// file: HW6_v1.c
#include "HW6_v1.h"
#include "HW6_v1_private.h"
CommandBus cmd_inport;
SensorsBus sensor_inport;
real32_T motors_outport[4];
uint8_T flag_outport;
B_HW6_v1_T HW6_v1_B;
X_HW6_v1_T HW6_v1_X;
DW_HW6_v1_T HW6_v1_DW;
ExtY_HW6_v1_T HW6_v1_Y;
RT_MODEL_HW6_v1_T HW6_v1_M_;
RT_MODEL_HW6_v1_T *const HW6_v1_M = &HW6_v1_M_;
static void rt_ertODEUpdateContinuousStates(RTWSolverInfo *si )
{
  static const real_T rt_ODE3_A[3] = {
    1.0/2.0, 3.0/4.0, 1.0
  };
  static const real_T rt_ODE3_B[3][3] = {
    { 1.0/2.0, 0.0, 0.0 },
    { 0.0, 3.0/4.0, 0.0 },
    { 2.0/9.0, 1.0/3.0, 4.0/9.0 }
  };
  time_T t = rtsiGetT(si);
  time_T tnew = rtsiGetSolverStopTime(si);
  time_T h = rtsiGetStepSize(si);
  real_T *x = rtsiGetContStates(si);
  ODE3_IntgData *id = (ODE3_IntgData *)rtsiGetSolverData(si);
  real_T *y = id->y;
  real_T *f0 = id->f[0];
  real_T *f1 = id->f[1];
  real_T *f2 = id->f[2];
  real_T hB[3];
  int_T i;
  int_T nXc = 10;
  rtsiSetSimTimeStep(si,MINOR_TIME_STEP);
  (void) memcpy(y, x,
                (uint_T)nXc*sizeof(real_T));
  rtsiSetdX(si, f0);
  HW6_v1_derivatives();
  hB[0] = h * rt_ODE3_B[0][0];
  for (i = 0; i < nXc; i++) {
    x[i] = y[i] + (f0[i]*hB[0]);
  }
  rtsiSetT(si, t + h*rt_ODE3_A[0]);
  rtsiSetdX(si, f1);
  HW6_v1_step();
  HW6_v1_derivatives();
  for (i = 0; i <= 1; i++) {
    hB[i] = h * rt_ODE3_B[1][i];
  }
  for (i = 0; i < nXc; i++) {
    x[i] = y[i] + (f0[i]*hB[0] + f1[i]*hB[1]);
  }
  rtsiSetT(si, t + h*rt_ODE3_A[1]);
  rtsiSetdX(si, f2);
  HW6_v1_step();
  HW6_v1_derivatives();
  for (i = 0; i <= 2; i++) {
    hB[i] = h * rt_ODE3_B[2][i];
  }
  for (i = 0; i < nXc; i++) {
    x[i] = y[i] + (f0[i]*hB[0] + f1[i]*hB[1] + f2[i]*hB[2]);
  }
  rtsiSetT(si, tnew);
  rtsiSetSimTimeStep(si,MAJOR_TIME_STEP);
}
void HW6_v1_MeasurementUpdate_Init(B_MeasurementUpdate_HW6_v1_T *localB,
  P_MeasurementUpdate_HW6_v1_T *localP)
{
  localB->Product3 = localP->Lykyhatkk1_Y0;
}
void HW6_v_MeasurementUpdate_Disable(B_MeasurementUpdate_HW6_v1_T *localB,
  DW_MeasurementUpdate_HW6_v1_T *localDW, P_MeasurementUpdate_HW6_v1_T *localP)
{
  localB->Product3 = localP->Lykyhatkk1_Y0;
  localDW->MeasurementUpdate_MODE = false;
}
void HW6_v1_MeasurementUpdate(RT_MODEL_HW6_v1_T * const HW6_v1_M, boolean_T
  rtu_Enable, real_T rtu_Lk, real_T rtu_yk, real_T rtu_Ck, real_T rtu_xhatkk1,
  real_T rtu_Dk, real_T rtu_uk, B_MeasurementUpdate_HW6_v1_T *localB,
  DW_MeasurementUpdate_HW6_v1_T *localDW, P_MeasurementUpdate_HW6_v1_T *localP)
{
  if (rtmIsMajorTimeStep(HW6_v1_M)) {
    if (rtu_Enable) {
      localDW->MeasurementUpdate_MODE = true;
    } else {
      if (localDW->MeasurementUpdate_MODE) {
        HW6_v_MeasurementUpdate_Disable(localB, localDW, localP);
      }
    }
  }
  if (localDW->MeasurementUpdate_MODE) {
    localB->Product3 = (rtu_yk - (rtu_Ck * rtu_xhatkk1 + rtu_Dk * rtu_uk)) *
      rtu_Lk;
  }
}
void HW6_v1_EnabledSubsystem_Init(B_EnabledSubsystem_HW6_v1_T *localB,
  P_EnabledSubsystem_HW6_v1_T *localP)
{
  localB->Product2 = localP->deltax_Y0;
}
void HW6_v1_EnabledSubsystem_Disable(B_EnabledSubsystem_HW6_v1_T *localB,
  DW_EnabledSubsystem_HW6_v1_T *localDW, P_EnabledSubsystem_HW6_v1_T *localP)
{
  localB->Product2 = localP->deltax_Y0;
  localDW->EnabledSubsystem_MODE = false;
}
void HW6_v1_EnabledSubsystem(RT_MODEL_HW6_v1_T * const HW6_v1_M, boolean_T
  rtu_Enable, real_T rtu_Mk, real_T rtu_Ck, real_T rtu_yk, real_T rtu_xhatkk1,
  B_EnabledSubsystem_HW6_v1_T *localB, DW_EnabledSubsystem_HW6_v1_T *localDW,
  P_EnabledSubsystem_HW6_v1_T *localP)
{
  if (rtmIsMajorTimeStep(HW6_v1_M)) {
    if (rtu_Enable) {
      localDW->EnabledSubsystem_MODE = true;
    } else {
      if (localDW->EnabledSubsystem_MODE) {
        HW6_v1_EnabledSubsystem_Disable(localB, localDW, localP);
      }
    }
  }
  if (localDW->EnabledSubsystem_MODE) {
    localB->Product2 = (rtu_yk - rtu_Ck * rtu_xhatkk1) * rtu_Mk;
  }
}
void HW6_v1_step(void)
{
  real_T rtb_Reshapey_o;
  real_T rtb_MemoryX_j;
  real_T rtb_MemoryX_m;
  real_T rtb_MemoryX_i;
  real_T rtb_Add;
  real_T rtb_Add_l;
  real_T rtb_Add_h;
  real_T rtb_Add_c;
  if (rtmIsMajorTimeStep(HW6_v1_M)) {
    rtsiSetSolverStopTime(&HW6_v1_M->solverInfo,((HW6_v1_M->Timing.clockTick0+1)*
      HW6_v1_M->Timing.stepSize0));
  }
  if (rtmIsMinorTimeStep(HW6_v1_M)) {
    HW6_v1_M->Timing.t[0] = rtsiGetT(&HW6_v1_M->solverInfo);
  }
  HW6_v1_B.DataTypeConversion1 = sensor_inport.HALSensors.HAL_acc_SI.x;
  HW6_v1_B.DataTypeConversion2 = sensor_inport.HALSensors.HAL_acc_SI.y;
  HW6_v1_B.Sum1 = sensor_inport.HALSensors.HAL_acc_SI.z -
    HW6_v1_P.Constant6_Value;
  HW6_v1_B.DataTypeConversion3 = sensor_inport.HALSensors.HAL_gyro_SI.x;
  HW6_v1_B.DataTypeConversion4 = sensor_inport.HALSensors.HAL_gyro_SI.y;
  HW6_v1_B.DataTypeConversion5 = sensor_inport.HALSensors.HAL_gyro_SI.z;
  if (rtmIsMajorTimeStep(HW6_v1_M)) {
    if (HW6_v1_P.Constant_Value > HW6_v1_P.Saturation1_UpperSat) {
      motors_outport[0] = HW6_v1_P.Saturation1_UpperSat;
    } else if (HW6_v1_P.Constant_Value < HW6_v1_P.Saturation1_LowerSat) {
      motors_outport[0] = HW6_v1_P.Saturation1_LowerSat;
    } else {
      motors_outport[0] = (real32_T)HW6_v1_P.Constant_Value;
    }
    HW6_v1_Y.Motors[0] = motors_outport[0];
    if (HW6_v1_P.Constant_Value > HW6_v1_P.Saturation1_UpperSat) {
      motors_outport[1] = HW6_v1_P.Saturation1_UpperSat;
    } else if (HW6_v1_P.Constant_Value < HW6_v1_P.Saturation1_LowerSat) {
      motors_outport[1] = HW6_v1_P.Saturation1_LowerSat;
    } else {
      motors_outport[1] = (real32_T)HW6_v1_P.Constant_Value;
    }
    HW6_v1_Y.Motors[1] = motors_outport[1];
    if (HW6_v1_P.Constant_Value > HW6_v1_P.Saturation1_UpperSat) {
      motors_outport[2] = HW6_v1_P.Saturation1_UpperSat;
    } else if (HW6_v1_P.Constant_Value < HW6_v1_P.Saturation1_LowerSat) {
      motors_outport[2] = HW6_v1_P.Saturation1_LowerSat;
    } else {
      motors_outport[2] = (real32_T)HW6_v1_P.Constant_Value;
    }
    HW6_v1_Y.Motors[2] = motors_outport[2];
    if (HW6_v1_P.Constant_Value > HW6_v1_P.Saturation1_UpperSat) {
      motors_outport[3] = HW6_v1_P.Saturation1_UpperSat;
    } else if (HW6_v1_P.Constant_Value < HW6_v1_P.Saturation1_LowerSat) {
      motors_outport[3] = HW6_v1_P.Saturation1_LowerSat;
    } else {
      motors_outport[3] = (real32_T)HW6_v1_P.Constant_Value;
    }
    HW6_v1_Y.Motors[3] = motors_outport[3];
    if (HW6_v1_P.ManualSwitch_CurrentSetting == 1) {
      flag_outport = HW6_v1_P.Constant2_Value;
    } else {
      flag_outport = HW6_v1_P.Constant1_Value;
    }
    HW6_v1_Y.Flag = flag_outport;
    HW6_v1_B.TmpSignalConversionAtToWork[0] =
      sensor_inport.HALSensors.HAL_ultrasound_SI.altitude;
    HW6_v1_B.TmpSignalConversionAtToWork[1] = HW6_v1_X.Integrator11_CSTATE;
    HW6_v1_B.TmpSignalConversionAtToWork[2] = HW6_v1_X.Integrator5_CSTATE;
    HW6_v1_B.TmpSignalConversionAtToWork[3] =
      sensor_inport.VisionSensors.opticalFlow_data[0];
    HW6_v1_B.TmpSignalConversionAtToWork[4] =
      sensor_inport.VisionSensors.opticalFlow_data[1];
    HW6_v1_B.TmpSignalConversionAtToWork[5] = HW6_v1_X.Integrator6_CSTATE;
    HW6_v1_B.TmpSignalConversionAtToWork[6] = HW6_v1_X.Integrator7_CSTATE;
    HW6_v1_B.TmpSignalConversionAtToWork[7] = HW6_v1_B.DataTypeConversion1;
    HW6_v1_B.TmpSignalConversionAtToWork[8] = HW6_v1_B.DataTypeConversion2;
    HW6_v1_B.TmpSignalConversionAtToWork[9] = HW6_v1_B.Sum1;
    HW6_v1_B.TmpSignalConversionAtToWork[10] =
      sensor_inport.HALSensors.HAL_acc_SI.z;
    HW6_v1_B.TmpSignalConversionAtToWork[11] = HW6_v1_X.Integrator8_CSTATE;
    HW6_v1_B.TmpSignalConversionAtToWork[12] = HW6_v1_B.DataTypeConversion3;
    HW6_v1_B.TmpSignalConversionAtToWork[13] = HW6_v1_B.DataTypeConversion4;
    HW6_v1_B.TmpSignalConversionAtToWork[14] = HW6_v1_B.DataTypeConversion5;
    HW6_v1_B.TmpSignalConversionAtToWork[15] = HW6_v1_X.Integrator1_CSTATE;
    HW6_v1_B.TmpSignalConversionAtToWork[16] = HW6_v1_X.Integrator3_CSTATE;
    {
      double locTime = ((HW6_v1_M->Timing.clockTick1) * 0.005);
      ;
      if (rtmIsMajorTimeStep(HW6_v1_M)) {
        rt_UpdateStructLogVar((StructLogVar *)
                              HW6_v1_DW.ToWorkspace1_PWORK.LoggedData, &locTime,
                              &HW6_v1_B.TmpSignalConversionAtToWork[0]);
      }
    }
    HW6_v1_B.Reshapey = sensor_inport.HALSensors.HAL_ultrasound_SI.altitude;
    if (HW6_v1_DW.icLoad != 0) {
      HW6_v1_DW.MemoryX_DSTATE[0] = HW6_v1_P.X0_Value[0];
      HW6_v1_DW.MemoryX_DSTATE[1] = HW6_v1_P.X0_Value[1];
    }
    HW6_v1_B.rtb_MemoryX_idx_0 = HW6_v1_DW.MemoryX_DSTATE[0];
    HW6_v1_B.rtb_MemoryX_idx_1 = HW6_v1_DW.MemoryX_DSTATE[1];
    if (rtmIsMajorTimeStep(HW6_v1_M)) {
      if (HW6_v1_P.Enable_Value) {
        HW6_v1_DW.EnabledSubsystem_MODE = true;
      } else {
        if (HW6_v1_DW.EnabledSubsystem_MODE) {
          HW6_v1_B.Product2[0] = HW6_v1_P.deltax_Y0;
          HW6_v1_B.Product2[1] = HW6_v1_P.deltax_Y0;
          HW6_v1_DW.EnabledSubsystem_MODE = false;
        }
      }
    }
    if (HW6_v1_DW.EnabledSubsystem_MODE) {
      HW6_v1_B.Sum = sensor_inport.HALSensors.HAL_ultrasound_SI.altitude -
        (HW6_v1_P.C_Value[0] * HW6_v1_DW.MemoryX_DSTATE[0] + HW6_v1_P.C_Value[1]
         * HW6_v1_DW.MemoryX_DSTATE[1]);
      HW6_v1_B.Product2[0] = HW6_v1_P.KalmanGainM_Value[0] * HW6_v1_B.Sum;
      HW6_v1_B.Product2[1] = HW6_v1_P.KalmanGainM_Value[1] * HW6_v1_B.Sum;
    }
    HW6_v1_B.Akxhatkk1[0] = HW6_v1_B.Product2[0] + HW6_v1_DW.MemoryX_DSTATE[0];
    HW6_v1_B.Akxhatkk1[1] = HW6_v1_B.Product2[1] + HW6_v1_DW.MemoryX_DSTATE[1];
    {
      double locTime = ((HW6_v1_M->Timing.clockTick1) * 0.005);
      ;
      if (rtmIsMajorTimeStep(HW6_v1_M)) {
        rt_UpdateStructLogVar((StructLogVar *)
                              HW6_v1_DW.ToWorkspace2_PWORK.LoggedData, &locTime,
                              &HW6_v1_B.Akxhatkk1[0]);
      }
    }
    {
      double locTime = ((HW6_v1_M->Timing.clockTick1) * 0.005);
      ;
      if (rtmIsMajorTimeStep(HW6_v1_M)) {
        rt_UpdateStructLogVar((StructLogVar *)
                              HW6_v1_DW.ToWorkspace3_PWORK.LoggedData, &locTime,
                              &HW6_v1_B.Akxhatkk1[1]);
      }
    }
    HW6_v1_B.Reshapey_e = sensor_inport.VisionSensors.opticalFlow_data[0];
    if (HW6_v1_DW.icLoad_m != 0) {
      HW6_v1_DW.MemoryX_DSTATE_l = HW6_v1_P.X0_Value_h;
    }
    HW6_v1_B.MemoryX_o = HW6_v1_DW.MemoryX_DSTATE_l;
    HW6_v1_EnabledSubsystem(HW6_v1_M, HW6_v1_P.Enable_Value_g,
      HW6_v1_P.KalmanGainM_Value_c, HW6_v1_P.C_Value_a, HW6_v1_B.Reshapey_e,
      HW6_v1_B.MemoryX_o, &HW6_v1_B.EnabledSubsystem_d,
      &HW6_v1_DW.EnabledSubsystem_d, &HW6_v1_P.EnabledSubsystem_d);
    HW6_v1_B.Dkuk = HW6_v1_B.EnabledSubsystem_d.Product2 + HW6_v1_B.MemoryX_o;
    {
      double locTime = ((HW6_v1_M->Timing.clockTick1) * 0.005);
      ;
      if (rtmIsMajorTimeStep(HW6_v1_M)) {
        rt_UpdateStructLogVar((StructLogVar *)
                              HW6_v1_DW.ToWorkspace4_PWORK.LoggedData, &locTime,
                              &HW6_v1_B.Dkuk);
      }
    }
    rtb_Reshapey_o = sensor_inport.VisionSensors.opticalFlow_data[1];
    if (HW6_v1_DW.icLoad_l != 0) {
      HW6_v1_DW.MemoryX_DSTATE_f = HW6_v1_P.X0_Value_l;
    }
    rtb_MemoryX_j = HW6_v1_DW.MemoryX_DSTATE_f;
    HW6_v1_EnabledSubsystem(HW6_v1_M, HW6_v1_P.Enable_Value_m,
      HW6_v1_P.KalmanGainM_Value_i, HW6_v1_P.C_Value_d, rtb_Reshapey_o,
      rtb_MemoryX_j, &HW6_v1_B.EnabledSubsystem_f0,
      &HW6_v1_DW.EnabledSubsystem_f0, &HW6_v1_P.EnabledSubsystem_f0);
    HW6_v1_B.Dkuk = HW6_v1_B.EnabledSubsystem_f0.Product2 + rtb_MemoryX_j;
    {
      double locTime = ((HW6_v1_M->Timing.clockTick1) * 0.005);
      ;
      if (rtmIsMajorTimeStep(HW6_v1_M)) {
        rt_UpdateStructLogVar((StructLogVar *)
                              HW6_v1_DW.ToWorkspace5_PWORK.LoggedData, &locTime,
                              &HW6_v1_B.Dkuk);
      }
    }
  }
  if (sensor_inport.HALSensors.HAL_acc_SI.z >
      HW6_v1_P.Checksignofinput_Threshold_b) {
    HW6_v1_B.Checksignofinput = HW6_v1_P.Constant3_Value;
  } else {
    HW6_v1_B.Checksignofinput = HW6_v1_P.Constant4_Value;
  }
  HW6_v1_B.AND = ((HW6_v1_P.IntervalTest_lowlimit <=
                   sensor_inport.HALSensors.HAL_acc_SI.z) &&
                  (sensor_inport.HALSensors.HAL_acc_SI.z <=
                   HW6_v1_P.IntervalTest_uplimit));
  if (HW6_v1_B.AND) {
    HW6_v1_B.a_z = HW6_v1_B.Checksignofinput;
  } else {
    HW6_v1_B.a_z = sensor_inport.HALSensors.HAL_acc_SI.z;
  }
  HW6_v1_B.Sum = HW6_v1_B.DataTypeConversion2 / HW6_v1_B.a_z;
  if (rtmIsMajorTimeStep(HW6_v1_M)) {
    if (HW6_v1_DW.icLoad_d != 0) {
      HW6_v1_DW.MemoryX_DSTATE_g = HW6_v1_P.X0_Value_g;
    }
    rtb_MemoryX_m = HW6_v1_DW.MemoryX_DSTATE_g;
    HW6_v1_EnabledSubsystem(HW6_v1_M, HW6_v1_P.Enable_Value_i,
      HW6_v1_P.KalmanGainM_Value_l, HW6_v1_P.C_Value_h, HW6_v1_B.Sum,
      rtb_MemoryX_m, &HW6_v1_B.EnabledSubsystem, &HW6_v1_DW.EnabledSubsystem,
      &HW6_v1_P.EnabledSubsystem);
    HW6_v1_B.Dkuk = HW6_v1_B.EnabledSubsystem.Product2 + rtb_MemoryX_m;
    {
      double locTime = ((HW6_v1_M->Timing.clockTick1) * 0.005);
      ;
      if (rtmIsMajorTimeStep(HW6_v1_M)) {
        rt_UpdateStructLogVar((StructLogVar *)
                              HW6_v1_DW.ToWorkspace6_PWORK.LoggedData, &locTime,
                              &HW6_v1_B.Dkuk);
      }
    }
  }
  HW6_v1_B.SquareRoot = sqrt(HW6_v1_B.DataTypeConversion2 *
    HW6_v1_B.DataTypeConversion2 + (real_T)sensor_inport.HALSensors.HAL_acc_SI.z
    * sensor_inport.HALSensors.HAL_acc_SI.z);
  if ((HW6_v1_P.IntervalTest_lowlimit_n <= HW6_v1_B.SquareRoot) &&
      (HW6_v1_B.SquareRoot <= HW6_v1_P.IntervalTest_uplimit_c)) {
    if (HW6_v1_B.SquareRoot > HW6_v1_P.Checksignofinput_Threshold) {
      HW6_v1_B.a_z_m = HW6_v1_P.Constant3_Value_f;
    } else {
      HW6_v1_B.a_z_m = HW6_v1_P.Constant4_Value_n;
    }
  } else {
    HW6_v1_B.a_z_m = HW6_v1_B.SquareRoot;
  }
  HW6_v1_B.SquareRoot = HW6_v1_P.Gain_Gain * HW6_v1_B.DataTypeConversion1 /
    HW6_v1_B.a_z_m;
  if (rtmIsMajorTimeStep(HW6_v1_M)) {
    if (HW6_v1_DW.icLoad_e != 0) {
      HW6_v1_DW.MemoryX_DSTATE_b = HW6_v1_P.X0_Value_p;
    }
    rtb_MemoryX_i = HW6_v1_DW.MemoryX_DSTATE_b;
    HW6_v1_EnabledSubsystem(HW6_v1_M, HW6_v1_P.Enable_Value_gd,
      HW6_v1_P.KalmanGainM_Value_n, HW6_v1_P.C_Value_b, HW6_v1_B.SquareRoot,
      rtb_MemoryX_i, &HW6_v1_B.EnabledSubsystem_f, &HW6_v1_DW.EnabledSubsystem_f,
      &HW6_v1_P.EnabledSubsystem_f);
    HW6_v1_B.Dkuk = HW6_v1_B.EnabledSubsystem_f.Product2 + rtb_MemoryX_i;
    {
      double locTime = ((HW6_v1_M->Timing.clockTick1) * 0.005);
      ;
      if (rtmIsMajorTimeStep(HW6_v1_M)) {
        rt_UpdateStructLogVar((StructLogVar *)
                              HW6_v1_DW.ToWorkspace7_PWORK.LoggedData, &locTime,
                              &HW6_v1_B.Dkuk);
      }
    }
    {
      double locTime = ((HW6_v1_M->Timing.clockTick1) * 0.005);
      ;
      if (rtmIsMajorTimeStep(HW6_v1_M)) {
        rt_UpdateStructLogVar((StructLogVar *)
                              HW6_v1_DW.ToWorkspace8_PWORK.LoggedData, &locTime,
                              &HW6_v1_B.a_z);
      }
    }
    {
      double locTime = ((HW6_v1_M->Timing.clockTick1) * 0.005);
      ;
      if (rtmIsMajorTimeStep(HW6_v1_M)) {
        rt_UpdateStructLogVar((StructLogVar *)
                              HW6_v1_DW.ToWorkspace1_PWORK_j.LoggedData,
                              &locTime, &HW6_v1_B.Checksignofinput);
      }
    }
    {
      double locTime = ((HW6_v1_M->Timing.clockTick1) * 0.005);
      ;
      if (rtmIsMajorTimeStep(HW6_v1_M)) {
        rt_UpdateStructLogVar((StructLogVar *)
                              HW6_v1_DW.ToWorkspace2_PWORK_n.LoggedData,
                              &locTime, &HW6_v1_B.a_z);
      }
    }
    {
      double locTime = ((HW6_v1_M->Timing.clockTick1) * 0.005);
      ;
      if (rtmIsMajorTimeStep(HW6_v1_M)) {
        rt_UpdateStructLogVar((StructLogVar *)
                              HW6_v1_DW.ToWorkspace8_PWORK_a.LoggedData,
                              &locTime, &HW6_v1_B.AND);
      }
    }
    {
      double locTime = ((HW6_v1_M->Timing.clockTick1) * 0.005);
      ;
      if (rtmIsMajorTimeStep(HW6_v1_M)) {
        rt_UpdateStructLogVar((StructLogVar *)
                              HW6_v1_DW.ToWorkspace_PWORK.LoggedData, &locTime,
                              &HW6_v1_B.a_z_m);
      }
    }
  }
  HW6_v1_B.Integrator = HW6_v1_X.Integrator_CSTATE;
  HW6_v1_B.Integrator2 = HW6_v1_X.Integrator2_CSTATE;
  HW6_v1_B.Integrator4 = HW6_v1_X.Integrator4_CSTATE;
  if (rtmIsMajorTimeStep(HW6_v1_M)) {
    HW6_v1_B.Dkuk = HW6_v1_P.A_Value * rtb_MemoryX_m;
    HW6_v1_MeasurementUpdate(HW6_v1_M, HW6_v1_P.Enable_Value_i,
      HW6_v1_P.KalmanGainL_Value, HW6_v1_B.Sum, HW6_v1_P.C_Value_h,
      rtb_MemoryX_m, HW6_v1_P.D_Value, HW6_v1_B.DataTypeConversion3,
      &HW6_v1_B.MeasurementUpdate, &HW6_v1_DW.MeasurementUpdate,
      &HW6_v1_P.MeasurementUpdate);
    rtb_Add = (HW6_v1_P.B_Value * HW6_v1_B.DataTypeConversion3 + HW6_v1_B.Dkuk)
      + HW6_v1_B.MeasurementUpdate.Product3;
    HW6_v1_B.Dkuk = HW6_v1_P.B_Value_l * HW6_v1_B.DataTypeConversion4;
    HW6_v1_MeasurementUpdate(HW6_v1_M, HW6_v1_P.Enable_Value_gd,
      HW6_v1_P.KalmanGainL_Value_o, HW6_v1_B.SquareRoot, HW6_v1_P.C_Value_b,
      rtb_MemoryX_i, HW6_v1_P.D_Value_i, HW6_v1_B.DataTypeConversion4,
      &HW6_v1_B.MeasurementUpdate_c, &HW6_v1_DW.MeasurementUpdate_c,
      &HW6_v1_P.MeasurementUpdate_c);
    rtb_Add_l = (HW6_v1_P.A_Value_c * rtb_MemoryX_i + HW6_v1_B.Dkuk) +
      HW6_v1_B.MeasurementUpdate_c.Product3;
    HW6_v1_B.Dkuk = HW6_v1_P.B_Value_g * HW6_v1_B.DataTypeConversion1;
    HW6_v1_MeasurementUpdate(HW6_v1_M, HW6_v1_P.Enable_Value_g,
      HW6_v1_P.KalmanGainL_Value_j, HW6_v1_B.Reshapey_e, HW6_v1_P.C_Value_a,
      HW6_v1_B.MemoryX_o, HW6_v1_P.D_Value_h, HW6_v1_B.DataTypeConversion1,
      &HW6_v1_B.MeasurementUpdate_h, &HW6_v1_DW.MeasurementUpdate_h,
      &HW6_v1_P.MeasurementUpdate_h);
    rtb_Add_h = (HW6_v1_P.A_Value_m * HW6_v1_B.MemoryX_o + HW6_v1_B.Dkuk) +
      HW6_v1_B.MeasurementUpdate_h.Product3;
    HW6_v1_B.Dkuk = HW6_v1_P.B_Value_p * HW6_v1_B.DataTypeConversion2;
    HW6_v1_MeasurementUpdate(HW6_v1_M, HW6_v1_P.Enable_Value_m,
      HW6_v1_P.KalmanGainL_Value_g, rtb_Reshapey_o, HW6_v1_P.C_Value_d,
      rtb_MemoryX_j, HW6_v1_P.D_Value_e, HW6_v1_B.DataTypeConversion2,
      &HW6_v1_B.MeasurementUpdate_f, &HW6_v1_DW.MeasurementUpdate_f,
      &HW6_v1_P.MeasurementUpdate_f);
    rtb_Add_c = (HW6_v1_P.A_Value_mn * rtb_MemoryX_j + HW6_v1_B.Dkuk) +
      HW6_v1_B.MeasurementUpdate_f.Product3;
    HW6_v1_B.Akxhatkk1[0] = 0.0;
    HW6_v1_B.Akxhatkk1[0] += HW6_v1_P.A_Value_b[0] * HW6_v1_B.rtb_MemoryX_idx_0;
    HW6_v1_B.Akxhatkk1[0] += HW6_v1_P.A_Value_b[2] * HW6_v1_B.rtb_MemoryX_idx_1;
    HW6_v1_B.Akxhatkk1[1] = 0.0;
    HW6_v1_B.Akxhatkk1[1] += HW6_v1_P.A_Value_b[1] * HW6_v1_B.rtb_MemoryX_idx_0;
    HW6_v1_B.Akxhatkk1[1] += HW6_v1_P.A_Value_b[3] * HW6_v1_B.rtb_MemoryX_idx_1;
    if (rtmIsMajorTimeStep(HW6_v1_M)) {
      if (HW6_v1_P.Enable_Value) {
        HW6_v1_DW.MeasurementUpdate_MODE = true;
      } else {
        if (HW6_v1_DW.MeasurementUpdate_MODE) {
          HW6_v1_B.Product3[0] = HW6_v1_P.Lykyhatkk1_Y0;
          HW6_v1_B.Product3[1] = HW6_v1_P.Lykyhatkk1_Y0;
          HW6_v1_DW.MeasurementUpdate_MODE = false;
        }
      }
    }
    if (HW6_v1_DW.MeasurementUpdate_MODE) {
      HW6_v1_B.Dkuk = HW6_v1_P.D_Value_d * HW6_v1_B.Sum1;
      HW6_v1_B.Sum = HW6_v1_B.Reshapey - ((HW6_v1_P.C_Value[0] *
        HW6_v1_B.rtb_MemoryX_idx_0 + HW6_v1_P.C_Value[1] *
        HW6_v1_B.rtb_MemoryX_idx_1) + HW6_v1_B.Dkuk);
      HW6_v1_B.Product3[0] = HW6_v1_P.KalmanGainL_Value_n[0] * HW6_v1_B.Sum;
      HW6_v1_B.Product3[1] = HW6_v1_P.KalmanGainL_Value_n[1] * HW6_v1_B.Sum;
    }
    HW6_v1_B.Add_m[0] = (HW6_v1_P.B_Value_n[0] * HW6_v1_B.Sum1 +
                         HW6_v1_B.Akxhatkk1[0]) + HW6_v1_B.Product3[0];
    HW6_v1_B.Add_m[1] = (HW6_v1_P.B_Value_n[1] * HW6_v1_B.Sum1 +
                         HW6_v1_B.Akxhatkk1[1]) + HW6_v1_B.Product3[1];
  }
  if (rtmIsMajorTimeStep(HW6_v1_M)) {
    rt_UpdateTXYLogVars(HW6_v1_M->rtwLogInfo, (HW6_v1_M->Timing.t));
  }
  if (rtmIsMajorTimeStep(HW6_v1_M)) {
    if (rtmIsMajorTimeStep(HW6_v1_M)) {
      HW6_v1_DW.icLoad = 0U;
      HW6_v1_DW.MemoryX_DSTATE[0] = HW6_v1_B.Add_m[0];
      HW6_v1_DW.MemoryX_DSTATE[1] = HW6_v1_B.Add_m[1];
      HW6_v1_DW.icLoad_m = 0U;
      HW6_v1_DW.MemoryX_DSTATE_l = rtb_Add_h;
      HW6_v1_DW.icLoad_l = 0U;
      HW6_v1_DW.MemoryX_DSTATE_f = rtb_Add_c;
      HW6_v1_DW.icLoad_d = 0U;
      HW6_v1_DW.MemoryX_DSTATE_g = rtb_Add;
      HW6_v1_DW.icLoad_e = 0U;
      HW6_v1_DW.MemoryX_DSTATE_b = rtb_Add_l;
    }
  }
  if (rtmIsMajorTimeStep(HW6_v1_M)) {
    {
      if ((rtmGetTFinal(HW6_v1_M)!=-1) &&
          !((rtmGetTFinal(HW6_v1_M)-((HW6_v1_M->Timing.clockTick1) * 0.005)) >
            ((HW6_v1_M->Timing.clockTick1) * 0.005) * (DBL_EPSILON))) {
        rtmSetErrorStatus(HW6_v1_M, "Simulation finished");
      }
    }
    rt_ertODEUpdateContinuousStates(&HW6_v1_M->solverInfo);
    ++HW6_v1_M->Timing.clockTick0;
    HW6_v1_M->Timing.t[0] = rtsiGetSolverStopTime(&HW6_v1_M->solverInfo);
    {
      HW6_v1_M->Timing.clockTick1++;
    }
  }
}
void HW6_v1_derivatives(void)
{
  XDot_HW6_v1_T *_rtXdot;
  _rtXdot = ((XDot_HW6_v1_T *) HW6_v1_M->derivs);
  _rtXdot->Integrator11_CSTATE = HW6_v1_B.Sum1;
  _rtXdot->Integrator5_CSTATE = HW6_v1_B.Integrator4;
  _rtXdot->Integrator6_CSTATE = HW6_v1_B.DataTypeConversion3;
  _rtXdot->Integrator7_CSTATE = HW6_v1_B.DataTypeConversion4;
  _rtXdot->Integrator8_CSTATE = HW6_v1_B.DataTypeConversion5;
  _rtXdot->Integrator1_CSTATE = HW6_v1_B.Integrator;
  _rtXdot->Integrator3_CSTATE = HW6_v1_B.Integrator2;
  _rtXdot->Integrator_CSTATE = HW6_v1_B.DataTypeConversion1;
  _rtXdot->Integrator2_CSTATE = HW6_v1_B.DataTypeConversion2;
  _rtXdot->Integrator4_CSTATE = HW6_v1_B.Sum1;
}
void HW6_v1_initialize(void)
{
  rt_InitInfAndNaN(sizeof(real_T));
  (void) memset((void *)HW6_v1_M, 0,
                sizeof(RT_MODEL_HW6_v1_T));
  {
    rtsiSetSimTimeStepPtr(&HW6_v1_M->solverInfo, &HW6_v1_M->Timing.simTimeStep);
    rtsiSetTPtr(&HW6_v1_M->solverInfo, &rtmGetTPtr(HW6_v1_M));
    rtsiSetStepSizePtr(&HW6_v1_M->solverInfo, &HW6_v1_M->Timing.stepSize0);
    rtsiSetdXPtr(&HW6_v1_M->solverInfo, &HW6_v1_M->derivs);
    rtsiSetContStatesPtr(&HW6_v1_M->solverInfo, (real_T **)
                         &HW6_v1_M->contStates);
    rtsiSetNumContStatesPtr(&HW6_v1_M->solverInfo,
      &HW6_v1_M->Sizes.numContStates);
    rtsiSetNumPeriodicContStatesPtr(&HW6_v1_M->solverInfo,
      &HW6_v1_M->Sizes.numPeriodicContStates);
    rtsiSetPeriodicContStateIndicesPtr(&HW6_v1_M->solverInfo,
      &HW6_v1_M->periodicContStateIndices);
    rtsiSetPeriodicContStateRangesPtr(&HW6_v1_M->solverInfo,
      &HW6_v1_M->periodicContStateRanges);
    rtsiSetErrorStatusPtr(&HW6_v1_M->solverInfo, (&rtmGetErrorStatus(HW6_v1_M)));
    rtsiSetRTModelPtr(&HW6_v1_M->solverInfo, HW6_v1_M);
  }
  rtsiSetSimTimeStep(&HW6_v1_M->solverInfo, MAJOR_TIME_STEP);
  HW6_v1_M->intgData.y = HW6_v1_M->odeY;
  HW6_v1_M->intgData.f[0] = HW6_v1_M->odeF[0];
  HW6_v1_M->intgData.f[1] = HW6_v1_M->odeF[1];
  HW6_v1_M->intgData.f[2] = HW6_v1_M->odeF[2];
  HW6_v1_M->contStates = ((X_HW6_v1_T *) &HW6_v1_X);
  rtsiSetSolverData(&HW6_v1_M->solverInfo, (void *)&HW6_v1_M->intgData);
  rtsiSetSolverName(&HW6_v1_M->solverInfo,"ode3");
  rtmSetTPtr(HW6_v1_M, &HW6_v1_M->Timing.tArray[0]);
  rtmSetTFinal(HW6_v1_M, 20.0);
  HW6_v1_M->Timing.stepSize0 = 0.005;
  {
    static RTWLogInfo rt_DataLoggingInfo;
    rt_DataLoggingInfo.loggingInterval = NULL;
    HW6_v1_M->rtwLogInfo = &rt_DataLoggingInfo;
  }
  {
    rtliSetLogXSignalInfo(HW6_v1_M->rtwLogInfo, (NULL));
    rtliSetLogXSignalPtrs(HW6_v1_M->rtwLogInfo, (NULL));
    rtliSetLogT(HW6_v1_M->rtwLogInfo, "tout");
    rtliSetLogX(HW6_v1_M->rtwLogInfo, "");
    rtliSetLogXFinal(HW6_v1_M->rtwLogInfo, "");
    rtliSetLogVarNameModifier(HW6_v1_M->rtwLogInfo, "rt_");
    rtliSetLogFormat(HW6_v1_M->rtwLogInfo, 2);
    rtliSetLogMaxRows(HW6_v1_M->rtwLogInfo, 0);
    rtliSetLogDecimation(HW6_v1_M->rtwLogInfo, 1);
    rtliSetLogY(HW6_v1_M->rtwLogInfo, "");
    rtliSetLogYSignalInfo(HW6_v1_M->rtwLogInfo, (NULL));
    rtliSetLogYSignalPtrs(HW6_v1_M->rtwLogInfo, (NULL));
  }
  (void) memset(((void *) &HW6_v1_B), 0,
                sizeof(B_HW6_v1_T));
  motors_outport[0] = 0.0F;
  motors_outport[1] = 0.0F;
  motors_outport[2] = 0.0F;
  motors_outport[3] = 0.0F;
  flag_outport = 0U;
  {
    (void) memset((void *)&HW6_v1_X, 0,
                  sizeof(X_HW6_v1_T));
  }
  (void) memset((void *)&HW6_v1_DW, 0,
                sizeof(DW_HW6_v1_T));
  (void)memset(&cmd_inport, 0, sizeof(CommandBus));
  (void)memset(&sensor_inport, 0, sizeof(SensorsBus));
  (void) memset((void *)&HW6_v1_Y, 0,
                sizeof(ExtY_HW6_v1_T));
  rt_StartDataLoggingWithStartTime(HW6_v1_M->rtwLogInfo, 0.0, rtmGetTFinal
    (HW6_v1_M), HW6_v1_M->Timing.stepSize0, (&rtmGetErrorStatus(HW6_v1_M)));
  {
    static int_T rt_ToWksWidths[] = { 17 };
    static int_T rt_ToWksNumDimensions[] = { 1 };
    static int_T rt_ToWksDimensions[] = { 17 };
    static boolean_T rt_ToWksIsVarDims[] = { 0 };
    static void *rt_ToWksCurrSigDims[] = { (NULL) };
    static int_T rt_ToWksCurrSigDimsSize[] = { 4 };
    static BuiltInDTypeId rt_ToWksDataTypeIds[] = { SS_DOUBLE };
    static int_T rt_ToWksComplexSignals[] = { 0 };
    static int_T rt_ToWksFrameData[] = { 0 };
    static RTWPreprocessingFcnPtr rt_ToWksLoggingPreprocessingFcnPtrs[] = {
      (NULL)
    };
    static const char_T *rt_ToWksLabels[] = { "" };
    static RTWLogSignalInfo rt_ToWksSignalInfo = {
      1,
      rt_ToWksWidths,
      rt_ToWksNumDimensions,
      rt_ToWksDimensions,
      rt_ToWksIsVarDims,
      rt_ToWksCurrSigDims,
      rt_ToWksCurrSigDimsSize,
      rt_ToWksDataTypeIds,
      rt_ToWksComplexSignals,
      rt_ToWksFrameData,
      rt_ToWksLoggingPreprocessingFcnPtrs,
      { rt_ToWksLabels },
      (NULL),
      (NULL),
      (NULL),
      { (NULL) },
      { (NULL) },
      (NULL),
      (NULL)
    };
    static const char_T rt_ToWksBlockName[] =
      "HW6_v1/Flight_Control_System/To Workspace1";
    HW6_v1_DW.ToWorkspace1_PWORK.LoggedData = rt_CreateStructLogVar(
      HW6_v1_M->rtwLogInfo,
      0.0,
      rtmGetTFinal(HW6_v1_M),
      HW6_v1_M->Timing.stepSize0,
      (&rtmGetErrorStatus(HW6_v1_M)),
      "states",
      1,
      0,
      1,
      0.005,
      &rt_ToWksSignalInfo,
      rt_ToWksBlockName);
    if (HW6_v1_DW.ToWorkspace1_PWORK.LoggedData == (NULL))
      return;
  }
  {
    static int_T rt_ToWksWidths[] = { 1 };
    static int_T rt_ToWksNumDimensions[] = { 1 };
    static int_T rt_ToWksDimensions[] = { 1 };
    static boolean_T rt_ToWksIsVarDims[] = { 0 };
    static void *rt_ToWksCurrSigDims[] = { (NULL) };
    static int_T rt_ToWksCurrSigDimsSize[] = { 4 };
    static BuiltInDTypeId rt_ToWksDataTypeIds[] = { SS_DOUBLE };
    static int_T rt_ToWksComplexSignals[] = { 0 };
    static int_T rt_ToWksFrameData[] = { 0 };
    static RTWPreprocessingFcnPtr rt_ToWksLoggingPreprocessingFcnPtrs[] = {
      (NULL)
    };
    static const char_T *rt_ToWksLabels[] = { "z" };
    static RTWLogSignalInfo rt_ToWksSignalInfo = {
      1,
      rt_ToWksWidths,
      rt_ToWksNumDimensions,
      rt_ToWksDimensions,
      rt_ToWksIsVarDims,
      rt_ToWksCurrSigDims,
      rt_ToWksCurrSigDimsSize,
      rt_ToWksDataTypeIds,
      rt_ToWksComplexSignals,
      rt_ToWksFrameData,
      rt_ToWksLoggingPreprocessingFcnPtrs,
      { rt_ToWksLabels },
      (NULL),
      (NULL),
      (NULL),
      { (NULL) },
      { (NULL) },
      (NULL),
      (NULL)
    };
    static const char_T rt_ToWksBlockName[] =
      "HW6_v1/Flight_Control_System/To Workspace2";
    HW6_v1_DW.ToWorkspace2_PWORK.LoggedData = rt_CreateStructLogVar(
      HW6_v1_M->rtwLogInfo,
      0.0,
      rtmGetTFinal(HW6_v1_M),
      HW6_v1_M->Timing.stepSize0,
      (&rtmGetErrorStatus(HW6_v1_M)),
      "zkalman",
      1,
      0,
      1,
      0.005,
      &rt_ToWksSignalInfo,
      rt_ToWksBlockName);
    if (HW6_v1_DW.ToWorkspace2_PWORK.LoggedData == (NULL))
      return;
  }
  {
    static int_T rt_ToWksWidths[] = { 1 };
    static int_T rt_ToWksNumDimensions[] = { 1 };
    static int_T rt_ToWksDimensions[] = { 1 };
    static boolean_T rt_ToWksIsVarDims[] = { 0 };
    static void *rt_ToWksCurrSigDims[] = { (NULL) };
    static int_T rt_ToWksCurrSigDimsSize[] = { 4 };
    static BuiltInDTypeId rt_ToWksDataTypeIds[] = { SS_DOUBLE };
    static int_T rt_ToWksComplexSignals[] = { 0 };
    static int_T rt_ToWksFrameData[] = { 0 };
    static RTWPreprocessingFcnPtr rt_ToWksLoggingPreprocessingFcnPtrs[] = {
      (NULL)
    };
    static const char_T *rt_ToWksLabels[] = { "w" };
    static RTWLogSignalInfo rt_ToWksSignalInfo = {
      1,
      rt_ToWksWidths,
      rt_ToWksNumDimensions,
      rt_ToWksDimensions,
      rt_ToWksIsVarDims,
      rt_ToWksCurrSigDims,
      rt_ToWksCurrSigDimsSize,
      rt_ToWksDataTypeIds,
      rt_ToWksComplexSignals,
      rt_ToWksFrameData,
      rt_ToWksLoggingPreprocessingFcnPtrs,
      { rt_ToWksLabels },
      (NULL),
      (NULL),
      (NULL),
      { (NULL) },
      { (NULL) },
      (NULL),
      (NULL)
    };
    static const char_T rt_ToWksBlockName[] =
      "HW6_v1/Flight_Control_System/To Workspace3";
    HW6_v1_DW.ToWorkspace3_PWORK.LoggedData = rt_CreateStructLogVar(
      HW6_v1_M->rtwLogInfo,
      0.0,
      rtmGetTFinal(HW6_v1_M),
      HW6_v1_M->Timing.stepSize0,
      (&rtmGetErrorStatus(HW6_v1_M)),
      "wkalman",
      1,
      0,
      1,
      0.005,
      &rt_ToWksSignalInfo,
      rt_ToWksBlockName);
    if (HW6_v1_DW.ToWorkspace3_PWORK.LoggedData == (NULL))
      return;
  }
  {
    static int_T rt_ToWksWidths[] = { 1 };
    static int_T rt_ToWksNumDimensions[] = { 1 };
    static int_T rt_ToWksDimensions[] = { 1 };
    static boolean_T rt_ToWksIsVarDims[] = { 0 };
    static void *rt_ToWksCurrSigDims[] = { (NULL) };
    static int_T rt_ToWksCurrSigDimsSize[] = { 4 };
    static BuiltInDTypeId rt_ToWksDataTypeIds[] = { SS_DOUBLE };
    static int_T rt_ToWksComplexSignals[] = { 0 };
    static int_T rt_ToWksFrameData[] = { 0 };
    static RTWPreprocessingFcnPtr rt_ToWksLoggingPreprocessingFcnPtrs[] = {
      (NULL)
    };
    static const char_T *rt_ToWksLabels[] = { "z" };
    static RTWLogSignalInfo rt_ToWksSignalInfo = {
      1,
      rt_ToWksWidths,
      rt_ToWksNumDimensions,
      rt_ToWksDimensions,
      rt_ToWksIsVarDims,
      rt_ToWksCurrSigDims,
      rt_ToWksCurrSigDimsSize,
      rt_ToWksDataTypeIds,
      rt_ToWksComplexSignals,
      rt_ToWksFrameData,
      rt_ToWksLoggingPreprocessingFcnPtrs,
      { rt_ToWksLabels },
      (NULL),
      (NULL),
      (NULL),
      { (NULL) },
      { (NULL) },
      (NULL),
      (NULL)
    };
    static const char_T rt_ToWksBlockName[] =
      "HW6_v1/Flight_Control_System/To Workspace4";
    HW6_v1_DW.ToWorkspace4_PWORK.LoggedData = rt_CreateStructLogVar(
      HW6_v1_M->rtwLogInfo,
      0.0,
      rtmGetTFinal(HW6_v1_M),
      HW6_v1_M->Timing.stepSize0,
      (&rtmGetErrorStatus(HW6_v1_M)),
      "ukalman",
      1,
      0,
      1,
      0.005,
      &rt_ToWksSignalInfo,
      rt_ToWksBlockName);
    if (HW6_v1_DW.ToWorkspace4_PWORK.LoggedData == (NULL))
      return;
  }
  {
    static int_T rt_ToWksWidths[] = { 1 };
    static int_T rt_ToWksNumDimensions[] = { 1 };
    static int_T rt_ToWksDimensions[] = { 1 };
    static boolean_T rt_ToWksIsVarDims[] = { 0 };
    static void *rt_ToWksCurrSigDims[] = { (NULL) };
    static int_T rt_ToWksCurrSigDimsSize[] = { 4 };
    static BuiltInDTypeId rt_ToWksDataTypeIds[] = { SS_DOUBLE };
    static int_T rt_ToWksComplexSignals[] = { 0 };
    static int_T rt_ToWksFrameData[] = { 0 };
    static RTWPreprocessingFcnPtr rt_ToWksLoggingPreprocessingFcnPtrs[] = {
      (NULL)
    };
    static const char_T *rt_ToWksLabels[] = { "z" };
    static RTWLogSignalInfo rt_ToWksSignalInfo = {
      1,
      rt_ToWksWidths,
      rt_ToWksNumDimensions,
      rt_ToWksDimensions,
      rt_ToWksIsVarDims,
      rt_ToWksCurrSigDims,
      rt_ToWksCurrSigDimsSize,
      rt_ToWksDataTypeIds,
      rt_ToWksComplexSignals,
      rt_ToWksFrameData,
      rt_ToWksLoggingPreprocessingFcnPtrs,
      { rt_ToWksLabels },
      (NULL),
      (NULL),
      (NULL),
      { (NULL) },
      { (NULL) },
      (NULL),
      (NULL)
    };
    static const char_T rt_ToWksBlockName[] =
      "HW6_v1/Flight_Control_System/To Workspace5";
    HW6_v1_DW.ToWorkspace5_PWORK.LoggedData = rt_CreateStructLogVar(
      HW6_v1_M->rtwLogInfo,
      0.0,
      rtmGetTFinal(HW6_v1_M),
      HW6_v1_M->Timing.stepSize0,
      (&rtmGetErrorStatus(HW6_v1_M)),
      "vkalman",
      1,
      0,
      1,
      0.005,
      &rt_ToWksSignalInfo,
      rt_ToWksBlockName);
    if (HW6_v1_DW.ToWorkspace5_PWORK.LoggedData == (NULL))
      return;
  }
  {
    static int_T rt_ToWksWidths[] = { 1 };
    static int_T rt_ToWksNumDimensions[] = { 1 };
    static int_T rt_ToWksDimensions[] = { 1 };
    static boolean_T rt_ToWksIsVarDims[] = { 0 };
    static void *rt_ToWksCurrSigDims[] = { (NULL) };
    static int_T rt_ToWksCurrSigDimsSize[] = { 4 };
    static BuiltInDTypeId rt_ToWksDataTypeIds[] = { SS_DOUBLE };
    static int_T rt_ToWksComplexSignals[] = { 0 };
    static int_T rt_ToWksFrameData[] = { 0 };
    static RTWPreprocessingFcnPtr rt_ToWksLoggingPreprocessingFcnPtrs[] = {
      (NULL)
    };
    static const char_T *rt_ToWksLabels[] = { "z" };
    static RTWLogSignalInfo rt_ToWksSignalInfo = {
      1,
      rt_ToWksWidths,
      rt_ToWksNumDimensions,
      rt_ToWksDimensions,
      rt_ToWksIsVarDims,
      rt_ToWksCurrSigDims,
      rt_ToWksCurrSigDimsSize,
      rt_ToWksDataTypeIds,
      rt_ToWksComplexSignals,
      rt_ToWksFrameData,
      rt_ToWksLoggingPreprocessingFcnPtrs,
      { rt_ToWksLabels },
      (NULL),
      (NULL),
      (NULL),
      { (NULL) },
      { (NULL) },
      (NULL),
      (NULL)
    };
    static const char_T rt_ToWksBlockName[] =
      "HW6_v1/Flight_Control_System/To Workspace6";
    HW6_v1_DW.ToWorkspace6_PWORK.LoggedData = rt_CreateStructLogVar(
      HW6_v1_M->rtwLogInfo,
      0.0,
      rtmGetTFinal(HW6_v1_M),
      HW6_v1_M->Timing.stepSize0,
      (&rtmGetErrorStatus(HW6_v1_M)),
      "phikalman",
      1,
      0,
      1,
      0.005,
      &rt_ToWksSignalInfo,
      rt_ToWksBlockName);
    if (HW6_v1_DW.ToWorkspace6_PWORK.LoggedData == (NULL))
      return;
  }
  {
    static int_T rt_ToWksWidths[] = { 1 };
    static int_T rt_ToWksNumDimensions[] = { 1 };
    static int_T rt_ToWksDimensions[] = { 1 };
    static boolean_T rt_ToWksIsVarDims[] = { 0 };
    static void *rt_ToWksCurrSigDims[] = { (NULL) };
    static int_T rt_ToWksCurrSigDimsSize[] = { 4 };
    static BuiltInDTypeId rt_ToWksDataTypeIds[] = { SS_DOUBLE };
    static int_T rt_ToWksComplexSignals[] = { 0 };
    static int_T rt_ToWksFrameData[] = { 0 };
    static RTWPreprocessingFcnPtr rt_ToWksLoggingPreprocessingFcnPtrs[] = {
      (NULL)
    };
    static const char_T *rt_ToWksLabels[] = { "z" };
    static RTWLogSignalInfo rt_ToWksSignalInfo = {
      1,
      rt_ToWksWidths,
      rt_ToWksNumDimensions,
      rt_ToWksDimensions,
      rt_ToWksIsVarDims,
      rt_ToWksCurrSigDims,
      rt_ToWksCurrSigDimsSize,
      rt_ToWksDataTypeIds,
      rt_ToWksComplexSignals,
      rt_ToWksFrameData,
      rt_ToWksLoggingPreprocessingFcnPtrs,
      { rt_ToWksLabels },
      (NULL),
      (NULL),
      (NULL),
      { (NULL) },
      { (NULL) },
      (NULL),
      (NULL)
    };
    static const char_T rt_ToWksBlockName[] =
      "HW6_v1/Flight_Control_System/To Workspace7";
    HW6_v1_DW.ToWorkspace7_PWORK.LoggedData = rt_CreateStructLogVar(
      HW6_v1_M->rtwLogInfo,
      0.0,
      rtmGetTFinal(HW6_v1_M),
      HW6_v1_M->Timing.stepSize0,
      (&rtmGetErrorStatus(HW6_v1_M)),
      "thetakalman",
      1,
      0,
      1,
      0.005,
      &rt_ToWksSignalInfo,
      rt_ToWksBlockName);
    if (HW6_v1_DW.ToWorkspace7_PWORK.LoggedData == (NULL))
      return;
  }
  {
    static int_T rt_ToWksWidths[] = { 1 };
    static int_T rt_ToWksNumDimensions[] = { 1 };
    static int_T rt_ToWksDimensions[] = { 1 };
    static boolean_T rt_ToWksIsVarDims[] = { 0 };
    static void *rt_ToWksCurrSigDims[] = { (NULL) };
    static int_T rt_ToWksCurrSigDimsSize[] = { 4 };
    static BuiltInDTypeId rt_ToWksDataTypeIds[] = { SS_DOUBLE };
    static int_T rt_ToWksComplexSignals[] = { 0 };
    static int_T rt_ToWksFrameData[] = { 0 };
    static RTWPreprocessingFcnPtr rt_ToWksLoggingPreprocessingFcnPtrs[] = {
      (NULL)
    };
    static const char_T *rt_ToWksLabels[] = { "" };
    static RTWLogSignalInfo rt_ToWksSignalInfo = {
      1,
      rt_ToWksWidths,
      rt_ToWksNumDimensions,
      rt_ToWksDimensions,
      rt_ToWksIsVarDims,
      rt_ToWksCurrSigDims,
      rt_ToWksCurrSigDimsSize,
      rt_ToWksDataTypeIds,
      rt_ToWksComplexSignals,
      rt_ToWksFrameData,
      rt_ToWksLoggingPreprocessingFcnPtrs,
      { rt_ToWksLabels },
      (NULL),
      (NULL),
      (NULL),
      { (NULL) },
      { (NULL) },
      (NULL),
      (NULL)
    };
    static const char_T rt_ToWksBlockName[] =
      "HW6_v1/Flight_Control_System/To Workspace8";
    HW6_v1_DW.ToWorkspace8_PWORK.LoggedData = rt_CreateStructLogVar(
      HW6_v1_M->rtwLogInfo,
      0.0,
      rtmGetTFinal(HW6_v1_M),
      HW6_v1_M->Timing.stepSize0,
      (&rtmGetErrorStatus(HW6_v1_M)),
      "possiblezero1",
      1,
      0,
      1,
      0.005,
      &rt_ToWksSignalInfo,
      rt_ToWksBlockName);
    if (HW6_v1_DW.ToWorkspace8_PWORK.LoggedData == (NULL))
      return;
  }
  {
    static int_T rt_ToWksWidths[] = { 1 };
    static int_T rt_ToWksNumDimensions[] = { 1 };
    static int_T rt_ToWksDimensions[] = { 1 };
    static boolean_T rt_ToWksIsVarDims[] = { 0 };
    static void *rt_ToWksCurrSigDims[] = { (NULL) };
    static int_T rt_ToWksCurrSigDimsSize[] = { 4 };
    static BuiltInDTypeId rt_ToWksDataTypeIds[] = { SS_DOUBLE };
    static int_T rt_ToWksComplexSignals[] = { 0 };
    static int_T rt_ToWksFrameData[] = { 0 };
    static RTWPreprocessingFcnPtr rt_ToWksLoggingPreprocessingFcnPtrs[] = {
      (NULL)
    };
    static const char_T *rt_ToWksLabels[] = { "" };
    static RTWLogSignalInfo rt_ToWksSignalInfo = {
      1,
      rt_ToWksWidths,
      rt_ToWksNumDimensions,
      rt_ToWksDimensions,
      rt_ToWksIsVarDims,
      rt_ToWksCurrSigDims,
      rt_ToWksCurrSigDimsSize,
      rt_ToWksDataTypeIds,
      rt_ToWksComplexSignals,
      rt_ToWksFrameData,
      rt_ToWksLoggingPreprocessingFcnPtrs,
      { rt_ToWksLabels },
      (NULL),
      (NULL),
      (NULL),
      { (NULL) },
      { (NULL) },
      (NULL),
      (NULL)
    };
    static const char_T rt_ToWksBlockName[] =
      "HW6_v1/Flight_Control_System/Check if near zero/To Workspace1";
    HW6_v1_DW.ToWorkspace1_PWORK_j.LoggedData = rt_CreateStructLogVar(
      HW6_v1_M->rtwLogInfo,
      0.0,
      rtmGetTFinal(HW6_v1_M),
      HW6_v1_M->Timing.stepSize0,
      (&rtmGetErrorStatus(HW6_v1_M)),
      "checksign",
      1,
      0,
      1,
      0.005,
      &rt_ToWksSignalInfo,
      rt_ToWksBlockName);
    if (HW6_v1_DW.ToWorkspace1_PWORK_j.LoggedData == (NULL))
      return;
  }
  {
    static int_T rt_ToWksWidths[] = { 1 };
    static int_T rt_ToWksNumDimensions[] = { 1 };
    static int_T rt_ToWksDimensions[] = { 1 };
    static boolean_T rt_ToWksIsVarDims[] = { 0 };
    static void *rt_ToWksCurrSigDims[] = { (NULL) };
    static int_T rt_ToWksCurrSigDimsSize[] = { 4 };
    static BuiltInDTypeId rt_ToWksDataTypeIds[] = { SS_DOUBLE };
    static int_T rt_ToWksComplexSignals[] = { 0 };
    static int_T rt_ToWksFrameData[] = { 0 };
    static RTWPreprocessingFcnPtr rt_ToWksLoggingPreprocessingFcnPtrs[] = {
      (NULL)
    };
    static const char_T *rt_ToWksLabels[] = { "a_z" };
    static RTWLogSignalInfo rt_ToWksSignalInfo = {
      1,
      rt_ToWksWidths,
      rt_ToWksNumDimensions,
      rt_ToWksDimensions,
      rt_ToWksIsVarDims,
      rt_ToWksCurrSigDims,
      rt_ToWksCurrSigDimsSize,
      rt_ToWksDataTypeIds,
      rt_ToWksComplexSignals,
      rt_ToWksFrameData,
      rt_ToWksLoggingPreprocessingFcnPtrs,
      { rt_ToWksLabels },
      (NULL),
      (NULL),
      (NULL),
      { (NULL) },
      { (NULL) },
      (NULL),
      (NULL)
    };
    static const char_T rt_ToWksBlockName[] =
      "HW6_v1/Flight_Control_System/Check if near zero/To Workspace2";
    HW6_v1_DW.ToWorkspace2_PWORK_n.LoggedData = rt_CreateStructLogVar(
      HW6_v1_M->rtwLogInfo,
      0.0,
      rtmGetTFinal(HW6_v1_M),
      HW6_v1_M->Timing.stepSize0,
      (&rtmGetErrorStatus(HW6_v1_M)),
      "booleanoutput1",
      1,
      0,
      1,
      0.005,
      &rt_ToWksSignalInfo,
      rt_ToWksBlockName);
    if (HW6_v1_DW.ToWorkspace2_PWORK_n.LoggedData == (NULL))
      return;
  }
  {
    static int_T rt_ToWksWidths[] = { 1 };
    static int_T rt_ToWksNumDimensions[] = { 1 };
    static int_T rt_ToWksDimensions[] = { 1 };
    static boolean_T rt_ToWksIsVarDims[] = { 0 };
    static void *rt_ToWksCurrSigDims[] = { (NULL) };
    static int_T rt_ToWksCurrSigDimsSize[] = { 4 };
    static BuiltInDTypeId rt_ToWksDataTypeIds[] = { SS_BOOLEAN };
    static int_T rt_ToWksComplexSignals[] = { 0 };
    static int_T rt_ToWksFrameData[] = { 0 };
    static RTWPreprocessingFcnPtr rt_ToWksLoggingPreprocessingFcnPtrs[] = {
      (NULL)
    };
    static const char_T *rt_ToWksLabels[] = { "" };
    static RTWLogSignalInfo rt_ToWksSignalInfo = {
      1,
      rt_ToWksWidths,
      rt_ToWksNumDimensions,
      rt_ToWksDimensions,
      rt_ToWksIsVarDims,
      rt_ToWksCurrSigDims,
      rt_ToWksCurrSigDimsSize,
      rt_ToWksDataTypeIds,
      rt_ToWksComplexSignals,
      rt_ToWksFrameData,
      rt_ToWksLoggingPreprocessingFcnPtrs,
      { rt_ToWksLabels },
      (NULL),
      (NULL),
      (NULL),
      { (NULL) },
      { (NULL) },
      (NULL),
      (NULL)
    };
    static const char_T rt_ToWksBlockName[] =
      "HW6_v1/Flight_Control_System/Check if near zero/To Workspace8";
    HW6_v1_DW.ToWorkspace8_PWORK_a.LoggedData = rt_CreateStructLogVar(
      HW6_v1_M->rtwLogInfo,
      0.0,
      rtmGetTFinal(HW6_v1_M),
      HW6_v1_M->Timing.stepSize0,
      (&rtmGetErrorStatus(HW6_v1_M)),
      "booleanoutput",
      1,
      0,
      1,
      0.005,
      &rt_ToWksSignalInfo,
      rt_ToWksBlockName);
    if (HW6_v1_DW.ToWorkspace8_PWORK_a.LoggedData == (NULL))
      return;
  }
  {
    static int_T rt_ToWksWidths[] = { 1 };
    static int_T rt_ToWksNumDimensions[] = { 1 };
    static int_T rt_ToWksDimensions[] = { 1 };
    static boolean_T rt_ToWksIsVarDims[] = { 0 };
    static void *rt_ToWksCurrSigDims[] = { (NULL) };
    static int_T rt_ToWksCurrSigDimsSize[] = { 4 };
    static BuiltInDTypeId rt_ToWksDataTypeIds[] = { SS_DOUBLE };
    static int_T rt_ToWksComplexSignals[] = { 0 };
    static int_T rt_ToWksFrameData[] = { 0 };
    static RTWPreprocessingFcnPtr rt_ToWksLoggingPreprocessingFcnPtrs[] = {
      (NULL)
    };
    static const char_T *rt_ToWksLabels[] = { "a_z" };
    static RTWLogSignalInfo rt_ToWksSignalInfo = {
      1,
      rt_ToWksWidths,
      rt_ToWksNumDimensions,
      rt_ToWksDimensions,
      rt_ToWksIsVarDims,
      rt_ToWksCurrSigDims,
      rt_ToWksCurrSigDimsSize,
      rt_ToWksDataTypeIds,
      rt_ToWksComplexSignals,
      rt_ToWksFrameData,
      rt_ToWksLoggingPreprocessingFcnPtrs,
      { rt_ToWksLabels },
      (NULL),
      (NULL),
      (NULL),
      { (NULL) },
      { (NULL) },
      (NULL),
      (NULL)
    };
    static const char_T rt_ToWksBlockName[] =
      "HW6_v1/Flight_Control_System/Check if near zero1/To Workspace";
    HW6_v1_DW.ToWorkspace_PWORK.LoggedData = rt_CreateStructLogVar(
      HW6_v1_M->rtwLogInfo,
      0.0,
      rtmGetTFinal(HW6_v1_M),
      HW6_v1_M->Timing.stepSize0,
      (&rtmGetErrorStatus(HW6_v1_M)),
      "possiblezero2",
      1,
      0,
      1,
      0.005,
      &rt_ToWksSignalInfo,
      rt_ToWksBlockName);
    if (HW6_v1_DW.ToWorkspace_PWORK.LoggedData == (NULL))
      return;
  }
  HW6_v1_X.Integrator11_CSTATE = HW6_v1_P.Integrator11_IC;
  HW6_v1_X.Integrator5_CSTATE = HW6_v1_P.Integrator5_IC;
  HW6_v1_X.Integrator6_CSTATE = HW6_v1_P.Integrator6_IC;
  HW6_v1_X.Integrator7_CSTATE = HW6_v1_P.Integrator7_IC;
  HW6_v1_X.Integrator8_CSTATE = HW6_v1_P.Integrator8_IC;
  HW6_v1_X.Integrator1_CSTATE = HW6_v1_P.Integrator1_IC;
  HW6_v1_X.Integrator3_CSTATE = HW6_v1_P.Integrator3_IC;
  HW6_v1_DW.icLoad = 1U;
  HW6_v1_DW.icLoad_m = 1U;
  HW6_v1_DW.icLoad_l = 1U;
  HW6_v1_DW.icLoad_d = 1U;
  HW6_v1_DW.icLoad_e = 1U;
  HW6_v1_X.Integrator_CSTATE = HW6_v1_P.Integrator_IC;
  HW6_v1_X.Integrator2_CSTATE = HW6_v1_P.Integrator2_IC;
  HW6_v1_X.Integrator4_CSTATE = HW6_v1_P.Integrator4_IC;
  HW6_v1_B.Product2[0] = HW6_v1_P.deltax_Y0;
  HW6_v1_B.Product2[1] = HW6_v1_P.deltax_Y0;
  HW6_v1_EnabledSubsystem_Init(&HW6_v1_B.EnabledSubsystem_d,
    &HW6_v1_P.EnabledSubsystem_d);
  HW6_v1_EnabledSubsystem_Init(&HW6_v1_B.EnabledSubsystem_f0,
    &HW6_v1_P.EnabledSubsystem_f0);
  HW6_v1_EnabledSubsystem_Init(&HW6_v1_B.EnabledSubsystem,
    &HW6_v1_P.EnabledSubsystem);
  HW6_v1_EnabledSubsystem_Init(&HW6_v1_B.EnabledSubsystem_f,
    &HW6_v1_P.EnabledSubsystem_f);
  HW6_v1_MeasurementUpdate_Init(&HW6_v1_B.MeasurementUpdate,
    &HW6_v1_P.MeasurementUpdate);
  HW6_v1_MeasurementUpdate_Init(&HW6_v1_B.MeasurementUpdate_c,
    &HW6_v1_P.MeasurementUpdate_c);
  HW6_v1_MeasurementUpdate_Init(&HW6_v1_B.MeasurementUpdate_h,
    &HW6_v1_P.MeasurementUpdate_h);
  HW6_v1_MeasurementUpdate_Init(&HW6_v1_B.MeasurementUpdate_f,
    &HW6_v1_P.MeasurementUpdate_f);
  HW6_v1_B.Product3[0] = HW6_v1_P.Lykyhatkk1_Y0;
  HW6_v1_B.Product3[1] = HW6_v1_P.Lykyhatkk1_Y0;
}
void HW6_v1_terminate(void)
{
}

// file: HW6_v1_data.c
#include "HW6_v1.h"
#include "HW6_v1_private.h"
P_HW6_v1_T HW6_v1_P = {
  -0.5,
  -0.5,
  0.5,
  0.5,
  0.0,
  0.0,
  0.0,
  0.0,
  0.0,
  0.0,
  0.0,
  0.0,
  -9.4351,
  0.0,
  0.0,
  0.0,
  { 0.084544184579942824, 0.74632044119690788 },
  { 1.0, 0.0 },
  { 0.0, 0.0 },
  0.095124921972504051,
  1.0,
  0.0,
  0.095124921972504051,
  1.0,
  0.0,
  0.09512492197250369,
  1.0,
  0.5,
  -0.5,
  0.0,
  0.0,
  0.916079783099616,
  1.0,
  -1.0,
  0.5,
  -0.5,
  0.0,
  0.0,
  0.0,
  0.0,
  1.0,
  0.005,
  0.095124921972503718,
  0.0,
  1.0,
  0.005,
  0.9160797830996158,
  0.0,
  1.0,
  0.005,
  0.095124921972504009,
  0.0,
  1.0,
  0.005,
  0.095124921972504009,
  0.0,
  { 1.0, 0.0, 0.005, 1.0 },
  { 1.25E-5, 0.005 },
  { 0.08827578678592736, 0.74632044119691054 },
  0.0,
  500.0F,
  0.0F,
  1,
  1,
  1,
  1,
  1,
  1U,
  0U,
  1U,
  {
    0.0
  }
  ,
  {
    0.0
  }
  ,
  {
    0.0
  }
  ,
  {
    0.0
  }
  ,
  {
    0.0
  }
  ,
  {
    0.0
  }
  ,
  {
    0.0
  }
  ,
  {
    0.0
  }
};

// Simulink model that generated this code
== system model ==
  Inport#1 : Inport
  Inport#2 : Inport
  Motors : Outport  <- 1: Saturation1
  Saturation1 : Saturate  UpperLimit=500  LowerLimit=0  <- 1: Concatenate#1
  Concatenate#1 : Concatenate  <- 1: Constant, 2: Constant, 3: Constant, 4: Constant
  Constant : Constant  Value=0
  Flag : Outport  <- 1: ManualSwitch
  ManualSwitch : ManualSwitch  <- 1: Constant2, 2: Constant1
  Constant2 : Constant  Value=0
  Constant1 : Constant
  KalmanFilter#1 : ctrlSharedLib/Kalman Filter  TimeDomain=Discrete-Time  A=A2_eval  B=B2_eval  C=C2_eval  D=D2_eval  X0=[0]  N=0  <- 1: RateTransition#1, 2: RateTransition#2
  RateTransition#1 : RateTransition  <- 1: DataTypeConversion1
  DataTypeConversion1 : DataTypeConversion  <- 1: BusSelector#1
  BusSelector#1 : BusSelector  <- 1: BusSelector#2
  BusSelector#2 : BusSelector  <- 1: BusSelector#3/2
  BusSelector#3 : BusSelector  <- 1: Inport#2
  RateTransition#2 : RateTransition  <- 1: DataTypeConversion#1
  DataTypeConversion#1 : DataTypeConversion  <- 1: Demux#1
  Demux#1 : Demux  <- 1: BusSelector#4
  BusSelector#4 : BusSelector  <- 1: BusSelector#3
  KalmanFilter#2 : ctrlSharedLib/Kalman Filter  TimeDomain=Discrete-Time  A=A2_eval  B=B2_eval  C=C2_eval  D=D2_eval  X0=[0]  N=0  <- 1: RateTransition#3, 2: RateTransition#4
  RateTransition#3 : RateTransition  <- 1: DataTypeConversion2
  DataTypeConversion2 : DataTypeConversion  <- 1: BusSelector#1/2
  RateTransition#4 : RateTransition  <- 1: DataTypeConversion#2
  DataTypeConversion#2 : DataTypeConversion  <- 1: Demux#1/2
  KalmanFilter#3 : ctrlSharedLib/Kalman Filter  TimeDomain=Discrete-Time  A=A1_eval  B=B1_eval  C=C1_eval  D=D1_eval  X0=[0;0 ]  N=0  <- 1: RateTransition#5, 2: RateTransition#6
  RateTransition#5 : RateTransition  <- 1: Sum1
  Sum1 : Sum  Inputs=+-  <- 1: DataTypeConversion#3, 2: Constant6
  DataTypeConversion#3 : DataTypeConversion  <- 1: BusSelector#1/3
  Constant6 : Constant  Value=-9.4351
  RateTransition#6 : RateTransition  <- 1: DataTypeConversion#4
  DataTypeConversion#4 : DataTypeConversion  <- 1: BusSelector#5
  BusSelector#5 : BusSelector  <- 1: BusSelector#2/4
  Integrator1 : Integrator  <- 1: Integrator
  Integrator : Integrator  <- 1: DataTypeConversion1
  Integrator11 : Integrator  <- 1: Sum1
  Integrator3 : Integrator  <- 1: Integrator2
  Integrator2 : Integrator  <- 1: DataTypeConversion2
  Integrator5 : Integrator  <- 1: Integrator4
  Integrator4 : Integrator  <- 1: Sum1
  Integrator6 : Integrator  <- 1: DataTypeConversion3
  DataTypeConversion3 : DataTypeConversion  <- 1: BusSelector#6
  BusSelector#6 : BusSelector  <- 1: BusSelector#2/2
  Integrator7 : Integrator  <- 1: DataTypeConversion4
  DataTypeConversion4 : DataTypeConversion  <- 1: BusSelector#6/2
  Integrator8 : Integrator  <- 1: DataTypeConversion5
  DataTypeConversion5 : DataTypeConversion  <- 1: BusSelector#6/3
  KalmanFilter#4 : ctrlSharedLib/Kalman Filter  TimeDomain=Discrete-Time  A=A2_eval  B=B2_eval  C=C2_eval  D=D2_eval  X0=[0]  N=0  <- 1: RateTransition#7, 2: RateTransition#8
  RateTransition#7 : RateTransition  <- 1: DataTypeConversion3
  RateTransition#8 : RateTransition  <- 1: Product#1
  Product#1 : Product  Inputs=*/  <- 1: DataTypeConversion2, 2: Switch#1
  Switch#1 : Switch  Criteria=u2 > Threshold  <- 1: Checksignofinput, 2: IntervalTest, 3: DataTypeConversion#3
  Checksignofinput : Switch  Criteria=u2 > Threshold  <- 1: Constant3, 2: DataTypeConversion#3, 3: Constant4
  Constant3 : Constant  Value=0.5
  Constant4 : Constant  Value=-0.5
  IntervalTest : simulink/Logic and Bit Operations/Interval Test  uplimit=0.5  lowlimit=-0.5  <- 1: DataTypeConversion#3
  KalmanFilter#5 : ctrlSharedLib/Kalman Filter  TimeDomain=Discrete-Time  A=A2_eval  B=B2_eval  C=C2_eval  D=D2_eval  X0=[0]  N=0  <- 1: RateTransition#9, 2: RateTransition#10
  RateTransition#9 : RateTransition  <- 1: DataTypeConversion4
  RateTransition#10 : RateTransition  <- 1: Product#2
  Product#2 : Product  Inputs=*/  <- 1: Gain, 2: Switch#2
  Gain : Gain  Gain=-1  <- 1: DataTypeConversion1
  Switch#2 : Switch  Criteria=u2 > Threshold  <- 1: Switch#3, 2: IntervalTest#1, 3: SquareRoot
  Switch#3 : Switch  Criteria=u2 > Threshold  <- 1: Constant#1, 2: SquareRoot, 3: Constant#2
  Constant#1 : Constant  Value=0.5
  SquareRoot : Sqrt  <- 1: Sum#1
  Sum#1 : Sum  Inputs=++  <- 1: Math#1, 2: Math#2
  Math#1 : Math  Operator=square  <- 1: DataTypeConversion2
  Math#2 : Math  Operator=square  <- 1: DataTypeConversion#3
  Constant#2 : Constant  Value=-0.5
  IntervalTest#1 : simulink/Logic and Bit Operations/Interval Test  uplimit=0.5  lowlimit=-0.5  <- 1: SquareRoot
